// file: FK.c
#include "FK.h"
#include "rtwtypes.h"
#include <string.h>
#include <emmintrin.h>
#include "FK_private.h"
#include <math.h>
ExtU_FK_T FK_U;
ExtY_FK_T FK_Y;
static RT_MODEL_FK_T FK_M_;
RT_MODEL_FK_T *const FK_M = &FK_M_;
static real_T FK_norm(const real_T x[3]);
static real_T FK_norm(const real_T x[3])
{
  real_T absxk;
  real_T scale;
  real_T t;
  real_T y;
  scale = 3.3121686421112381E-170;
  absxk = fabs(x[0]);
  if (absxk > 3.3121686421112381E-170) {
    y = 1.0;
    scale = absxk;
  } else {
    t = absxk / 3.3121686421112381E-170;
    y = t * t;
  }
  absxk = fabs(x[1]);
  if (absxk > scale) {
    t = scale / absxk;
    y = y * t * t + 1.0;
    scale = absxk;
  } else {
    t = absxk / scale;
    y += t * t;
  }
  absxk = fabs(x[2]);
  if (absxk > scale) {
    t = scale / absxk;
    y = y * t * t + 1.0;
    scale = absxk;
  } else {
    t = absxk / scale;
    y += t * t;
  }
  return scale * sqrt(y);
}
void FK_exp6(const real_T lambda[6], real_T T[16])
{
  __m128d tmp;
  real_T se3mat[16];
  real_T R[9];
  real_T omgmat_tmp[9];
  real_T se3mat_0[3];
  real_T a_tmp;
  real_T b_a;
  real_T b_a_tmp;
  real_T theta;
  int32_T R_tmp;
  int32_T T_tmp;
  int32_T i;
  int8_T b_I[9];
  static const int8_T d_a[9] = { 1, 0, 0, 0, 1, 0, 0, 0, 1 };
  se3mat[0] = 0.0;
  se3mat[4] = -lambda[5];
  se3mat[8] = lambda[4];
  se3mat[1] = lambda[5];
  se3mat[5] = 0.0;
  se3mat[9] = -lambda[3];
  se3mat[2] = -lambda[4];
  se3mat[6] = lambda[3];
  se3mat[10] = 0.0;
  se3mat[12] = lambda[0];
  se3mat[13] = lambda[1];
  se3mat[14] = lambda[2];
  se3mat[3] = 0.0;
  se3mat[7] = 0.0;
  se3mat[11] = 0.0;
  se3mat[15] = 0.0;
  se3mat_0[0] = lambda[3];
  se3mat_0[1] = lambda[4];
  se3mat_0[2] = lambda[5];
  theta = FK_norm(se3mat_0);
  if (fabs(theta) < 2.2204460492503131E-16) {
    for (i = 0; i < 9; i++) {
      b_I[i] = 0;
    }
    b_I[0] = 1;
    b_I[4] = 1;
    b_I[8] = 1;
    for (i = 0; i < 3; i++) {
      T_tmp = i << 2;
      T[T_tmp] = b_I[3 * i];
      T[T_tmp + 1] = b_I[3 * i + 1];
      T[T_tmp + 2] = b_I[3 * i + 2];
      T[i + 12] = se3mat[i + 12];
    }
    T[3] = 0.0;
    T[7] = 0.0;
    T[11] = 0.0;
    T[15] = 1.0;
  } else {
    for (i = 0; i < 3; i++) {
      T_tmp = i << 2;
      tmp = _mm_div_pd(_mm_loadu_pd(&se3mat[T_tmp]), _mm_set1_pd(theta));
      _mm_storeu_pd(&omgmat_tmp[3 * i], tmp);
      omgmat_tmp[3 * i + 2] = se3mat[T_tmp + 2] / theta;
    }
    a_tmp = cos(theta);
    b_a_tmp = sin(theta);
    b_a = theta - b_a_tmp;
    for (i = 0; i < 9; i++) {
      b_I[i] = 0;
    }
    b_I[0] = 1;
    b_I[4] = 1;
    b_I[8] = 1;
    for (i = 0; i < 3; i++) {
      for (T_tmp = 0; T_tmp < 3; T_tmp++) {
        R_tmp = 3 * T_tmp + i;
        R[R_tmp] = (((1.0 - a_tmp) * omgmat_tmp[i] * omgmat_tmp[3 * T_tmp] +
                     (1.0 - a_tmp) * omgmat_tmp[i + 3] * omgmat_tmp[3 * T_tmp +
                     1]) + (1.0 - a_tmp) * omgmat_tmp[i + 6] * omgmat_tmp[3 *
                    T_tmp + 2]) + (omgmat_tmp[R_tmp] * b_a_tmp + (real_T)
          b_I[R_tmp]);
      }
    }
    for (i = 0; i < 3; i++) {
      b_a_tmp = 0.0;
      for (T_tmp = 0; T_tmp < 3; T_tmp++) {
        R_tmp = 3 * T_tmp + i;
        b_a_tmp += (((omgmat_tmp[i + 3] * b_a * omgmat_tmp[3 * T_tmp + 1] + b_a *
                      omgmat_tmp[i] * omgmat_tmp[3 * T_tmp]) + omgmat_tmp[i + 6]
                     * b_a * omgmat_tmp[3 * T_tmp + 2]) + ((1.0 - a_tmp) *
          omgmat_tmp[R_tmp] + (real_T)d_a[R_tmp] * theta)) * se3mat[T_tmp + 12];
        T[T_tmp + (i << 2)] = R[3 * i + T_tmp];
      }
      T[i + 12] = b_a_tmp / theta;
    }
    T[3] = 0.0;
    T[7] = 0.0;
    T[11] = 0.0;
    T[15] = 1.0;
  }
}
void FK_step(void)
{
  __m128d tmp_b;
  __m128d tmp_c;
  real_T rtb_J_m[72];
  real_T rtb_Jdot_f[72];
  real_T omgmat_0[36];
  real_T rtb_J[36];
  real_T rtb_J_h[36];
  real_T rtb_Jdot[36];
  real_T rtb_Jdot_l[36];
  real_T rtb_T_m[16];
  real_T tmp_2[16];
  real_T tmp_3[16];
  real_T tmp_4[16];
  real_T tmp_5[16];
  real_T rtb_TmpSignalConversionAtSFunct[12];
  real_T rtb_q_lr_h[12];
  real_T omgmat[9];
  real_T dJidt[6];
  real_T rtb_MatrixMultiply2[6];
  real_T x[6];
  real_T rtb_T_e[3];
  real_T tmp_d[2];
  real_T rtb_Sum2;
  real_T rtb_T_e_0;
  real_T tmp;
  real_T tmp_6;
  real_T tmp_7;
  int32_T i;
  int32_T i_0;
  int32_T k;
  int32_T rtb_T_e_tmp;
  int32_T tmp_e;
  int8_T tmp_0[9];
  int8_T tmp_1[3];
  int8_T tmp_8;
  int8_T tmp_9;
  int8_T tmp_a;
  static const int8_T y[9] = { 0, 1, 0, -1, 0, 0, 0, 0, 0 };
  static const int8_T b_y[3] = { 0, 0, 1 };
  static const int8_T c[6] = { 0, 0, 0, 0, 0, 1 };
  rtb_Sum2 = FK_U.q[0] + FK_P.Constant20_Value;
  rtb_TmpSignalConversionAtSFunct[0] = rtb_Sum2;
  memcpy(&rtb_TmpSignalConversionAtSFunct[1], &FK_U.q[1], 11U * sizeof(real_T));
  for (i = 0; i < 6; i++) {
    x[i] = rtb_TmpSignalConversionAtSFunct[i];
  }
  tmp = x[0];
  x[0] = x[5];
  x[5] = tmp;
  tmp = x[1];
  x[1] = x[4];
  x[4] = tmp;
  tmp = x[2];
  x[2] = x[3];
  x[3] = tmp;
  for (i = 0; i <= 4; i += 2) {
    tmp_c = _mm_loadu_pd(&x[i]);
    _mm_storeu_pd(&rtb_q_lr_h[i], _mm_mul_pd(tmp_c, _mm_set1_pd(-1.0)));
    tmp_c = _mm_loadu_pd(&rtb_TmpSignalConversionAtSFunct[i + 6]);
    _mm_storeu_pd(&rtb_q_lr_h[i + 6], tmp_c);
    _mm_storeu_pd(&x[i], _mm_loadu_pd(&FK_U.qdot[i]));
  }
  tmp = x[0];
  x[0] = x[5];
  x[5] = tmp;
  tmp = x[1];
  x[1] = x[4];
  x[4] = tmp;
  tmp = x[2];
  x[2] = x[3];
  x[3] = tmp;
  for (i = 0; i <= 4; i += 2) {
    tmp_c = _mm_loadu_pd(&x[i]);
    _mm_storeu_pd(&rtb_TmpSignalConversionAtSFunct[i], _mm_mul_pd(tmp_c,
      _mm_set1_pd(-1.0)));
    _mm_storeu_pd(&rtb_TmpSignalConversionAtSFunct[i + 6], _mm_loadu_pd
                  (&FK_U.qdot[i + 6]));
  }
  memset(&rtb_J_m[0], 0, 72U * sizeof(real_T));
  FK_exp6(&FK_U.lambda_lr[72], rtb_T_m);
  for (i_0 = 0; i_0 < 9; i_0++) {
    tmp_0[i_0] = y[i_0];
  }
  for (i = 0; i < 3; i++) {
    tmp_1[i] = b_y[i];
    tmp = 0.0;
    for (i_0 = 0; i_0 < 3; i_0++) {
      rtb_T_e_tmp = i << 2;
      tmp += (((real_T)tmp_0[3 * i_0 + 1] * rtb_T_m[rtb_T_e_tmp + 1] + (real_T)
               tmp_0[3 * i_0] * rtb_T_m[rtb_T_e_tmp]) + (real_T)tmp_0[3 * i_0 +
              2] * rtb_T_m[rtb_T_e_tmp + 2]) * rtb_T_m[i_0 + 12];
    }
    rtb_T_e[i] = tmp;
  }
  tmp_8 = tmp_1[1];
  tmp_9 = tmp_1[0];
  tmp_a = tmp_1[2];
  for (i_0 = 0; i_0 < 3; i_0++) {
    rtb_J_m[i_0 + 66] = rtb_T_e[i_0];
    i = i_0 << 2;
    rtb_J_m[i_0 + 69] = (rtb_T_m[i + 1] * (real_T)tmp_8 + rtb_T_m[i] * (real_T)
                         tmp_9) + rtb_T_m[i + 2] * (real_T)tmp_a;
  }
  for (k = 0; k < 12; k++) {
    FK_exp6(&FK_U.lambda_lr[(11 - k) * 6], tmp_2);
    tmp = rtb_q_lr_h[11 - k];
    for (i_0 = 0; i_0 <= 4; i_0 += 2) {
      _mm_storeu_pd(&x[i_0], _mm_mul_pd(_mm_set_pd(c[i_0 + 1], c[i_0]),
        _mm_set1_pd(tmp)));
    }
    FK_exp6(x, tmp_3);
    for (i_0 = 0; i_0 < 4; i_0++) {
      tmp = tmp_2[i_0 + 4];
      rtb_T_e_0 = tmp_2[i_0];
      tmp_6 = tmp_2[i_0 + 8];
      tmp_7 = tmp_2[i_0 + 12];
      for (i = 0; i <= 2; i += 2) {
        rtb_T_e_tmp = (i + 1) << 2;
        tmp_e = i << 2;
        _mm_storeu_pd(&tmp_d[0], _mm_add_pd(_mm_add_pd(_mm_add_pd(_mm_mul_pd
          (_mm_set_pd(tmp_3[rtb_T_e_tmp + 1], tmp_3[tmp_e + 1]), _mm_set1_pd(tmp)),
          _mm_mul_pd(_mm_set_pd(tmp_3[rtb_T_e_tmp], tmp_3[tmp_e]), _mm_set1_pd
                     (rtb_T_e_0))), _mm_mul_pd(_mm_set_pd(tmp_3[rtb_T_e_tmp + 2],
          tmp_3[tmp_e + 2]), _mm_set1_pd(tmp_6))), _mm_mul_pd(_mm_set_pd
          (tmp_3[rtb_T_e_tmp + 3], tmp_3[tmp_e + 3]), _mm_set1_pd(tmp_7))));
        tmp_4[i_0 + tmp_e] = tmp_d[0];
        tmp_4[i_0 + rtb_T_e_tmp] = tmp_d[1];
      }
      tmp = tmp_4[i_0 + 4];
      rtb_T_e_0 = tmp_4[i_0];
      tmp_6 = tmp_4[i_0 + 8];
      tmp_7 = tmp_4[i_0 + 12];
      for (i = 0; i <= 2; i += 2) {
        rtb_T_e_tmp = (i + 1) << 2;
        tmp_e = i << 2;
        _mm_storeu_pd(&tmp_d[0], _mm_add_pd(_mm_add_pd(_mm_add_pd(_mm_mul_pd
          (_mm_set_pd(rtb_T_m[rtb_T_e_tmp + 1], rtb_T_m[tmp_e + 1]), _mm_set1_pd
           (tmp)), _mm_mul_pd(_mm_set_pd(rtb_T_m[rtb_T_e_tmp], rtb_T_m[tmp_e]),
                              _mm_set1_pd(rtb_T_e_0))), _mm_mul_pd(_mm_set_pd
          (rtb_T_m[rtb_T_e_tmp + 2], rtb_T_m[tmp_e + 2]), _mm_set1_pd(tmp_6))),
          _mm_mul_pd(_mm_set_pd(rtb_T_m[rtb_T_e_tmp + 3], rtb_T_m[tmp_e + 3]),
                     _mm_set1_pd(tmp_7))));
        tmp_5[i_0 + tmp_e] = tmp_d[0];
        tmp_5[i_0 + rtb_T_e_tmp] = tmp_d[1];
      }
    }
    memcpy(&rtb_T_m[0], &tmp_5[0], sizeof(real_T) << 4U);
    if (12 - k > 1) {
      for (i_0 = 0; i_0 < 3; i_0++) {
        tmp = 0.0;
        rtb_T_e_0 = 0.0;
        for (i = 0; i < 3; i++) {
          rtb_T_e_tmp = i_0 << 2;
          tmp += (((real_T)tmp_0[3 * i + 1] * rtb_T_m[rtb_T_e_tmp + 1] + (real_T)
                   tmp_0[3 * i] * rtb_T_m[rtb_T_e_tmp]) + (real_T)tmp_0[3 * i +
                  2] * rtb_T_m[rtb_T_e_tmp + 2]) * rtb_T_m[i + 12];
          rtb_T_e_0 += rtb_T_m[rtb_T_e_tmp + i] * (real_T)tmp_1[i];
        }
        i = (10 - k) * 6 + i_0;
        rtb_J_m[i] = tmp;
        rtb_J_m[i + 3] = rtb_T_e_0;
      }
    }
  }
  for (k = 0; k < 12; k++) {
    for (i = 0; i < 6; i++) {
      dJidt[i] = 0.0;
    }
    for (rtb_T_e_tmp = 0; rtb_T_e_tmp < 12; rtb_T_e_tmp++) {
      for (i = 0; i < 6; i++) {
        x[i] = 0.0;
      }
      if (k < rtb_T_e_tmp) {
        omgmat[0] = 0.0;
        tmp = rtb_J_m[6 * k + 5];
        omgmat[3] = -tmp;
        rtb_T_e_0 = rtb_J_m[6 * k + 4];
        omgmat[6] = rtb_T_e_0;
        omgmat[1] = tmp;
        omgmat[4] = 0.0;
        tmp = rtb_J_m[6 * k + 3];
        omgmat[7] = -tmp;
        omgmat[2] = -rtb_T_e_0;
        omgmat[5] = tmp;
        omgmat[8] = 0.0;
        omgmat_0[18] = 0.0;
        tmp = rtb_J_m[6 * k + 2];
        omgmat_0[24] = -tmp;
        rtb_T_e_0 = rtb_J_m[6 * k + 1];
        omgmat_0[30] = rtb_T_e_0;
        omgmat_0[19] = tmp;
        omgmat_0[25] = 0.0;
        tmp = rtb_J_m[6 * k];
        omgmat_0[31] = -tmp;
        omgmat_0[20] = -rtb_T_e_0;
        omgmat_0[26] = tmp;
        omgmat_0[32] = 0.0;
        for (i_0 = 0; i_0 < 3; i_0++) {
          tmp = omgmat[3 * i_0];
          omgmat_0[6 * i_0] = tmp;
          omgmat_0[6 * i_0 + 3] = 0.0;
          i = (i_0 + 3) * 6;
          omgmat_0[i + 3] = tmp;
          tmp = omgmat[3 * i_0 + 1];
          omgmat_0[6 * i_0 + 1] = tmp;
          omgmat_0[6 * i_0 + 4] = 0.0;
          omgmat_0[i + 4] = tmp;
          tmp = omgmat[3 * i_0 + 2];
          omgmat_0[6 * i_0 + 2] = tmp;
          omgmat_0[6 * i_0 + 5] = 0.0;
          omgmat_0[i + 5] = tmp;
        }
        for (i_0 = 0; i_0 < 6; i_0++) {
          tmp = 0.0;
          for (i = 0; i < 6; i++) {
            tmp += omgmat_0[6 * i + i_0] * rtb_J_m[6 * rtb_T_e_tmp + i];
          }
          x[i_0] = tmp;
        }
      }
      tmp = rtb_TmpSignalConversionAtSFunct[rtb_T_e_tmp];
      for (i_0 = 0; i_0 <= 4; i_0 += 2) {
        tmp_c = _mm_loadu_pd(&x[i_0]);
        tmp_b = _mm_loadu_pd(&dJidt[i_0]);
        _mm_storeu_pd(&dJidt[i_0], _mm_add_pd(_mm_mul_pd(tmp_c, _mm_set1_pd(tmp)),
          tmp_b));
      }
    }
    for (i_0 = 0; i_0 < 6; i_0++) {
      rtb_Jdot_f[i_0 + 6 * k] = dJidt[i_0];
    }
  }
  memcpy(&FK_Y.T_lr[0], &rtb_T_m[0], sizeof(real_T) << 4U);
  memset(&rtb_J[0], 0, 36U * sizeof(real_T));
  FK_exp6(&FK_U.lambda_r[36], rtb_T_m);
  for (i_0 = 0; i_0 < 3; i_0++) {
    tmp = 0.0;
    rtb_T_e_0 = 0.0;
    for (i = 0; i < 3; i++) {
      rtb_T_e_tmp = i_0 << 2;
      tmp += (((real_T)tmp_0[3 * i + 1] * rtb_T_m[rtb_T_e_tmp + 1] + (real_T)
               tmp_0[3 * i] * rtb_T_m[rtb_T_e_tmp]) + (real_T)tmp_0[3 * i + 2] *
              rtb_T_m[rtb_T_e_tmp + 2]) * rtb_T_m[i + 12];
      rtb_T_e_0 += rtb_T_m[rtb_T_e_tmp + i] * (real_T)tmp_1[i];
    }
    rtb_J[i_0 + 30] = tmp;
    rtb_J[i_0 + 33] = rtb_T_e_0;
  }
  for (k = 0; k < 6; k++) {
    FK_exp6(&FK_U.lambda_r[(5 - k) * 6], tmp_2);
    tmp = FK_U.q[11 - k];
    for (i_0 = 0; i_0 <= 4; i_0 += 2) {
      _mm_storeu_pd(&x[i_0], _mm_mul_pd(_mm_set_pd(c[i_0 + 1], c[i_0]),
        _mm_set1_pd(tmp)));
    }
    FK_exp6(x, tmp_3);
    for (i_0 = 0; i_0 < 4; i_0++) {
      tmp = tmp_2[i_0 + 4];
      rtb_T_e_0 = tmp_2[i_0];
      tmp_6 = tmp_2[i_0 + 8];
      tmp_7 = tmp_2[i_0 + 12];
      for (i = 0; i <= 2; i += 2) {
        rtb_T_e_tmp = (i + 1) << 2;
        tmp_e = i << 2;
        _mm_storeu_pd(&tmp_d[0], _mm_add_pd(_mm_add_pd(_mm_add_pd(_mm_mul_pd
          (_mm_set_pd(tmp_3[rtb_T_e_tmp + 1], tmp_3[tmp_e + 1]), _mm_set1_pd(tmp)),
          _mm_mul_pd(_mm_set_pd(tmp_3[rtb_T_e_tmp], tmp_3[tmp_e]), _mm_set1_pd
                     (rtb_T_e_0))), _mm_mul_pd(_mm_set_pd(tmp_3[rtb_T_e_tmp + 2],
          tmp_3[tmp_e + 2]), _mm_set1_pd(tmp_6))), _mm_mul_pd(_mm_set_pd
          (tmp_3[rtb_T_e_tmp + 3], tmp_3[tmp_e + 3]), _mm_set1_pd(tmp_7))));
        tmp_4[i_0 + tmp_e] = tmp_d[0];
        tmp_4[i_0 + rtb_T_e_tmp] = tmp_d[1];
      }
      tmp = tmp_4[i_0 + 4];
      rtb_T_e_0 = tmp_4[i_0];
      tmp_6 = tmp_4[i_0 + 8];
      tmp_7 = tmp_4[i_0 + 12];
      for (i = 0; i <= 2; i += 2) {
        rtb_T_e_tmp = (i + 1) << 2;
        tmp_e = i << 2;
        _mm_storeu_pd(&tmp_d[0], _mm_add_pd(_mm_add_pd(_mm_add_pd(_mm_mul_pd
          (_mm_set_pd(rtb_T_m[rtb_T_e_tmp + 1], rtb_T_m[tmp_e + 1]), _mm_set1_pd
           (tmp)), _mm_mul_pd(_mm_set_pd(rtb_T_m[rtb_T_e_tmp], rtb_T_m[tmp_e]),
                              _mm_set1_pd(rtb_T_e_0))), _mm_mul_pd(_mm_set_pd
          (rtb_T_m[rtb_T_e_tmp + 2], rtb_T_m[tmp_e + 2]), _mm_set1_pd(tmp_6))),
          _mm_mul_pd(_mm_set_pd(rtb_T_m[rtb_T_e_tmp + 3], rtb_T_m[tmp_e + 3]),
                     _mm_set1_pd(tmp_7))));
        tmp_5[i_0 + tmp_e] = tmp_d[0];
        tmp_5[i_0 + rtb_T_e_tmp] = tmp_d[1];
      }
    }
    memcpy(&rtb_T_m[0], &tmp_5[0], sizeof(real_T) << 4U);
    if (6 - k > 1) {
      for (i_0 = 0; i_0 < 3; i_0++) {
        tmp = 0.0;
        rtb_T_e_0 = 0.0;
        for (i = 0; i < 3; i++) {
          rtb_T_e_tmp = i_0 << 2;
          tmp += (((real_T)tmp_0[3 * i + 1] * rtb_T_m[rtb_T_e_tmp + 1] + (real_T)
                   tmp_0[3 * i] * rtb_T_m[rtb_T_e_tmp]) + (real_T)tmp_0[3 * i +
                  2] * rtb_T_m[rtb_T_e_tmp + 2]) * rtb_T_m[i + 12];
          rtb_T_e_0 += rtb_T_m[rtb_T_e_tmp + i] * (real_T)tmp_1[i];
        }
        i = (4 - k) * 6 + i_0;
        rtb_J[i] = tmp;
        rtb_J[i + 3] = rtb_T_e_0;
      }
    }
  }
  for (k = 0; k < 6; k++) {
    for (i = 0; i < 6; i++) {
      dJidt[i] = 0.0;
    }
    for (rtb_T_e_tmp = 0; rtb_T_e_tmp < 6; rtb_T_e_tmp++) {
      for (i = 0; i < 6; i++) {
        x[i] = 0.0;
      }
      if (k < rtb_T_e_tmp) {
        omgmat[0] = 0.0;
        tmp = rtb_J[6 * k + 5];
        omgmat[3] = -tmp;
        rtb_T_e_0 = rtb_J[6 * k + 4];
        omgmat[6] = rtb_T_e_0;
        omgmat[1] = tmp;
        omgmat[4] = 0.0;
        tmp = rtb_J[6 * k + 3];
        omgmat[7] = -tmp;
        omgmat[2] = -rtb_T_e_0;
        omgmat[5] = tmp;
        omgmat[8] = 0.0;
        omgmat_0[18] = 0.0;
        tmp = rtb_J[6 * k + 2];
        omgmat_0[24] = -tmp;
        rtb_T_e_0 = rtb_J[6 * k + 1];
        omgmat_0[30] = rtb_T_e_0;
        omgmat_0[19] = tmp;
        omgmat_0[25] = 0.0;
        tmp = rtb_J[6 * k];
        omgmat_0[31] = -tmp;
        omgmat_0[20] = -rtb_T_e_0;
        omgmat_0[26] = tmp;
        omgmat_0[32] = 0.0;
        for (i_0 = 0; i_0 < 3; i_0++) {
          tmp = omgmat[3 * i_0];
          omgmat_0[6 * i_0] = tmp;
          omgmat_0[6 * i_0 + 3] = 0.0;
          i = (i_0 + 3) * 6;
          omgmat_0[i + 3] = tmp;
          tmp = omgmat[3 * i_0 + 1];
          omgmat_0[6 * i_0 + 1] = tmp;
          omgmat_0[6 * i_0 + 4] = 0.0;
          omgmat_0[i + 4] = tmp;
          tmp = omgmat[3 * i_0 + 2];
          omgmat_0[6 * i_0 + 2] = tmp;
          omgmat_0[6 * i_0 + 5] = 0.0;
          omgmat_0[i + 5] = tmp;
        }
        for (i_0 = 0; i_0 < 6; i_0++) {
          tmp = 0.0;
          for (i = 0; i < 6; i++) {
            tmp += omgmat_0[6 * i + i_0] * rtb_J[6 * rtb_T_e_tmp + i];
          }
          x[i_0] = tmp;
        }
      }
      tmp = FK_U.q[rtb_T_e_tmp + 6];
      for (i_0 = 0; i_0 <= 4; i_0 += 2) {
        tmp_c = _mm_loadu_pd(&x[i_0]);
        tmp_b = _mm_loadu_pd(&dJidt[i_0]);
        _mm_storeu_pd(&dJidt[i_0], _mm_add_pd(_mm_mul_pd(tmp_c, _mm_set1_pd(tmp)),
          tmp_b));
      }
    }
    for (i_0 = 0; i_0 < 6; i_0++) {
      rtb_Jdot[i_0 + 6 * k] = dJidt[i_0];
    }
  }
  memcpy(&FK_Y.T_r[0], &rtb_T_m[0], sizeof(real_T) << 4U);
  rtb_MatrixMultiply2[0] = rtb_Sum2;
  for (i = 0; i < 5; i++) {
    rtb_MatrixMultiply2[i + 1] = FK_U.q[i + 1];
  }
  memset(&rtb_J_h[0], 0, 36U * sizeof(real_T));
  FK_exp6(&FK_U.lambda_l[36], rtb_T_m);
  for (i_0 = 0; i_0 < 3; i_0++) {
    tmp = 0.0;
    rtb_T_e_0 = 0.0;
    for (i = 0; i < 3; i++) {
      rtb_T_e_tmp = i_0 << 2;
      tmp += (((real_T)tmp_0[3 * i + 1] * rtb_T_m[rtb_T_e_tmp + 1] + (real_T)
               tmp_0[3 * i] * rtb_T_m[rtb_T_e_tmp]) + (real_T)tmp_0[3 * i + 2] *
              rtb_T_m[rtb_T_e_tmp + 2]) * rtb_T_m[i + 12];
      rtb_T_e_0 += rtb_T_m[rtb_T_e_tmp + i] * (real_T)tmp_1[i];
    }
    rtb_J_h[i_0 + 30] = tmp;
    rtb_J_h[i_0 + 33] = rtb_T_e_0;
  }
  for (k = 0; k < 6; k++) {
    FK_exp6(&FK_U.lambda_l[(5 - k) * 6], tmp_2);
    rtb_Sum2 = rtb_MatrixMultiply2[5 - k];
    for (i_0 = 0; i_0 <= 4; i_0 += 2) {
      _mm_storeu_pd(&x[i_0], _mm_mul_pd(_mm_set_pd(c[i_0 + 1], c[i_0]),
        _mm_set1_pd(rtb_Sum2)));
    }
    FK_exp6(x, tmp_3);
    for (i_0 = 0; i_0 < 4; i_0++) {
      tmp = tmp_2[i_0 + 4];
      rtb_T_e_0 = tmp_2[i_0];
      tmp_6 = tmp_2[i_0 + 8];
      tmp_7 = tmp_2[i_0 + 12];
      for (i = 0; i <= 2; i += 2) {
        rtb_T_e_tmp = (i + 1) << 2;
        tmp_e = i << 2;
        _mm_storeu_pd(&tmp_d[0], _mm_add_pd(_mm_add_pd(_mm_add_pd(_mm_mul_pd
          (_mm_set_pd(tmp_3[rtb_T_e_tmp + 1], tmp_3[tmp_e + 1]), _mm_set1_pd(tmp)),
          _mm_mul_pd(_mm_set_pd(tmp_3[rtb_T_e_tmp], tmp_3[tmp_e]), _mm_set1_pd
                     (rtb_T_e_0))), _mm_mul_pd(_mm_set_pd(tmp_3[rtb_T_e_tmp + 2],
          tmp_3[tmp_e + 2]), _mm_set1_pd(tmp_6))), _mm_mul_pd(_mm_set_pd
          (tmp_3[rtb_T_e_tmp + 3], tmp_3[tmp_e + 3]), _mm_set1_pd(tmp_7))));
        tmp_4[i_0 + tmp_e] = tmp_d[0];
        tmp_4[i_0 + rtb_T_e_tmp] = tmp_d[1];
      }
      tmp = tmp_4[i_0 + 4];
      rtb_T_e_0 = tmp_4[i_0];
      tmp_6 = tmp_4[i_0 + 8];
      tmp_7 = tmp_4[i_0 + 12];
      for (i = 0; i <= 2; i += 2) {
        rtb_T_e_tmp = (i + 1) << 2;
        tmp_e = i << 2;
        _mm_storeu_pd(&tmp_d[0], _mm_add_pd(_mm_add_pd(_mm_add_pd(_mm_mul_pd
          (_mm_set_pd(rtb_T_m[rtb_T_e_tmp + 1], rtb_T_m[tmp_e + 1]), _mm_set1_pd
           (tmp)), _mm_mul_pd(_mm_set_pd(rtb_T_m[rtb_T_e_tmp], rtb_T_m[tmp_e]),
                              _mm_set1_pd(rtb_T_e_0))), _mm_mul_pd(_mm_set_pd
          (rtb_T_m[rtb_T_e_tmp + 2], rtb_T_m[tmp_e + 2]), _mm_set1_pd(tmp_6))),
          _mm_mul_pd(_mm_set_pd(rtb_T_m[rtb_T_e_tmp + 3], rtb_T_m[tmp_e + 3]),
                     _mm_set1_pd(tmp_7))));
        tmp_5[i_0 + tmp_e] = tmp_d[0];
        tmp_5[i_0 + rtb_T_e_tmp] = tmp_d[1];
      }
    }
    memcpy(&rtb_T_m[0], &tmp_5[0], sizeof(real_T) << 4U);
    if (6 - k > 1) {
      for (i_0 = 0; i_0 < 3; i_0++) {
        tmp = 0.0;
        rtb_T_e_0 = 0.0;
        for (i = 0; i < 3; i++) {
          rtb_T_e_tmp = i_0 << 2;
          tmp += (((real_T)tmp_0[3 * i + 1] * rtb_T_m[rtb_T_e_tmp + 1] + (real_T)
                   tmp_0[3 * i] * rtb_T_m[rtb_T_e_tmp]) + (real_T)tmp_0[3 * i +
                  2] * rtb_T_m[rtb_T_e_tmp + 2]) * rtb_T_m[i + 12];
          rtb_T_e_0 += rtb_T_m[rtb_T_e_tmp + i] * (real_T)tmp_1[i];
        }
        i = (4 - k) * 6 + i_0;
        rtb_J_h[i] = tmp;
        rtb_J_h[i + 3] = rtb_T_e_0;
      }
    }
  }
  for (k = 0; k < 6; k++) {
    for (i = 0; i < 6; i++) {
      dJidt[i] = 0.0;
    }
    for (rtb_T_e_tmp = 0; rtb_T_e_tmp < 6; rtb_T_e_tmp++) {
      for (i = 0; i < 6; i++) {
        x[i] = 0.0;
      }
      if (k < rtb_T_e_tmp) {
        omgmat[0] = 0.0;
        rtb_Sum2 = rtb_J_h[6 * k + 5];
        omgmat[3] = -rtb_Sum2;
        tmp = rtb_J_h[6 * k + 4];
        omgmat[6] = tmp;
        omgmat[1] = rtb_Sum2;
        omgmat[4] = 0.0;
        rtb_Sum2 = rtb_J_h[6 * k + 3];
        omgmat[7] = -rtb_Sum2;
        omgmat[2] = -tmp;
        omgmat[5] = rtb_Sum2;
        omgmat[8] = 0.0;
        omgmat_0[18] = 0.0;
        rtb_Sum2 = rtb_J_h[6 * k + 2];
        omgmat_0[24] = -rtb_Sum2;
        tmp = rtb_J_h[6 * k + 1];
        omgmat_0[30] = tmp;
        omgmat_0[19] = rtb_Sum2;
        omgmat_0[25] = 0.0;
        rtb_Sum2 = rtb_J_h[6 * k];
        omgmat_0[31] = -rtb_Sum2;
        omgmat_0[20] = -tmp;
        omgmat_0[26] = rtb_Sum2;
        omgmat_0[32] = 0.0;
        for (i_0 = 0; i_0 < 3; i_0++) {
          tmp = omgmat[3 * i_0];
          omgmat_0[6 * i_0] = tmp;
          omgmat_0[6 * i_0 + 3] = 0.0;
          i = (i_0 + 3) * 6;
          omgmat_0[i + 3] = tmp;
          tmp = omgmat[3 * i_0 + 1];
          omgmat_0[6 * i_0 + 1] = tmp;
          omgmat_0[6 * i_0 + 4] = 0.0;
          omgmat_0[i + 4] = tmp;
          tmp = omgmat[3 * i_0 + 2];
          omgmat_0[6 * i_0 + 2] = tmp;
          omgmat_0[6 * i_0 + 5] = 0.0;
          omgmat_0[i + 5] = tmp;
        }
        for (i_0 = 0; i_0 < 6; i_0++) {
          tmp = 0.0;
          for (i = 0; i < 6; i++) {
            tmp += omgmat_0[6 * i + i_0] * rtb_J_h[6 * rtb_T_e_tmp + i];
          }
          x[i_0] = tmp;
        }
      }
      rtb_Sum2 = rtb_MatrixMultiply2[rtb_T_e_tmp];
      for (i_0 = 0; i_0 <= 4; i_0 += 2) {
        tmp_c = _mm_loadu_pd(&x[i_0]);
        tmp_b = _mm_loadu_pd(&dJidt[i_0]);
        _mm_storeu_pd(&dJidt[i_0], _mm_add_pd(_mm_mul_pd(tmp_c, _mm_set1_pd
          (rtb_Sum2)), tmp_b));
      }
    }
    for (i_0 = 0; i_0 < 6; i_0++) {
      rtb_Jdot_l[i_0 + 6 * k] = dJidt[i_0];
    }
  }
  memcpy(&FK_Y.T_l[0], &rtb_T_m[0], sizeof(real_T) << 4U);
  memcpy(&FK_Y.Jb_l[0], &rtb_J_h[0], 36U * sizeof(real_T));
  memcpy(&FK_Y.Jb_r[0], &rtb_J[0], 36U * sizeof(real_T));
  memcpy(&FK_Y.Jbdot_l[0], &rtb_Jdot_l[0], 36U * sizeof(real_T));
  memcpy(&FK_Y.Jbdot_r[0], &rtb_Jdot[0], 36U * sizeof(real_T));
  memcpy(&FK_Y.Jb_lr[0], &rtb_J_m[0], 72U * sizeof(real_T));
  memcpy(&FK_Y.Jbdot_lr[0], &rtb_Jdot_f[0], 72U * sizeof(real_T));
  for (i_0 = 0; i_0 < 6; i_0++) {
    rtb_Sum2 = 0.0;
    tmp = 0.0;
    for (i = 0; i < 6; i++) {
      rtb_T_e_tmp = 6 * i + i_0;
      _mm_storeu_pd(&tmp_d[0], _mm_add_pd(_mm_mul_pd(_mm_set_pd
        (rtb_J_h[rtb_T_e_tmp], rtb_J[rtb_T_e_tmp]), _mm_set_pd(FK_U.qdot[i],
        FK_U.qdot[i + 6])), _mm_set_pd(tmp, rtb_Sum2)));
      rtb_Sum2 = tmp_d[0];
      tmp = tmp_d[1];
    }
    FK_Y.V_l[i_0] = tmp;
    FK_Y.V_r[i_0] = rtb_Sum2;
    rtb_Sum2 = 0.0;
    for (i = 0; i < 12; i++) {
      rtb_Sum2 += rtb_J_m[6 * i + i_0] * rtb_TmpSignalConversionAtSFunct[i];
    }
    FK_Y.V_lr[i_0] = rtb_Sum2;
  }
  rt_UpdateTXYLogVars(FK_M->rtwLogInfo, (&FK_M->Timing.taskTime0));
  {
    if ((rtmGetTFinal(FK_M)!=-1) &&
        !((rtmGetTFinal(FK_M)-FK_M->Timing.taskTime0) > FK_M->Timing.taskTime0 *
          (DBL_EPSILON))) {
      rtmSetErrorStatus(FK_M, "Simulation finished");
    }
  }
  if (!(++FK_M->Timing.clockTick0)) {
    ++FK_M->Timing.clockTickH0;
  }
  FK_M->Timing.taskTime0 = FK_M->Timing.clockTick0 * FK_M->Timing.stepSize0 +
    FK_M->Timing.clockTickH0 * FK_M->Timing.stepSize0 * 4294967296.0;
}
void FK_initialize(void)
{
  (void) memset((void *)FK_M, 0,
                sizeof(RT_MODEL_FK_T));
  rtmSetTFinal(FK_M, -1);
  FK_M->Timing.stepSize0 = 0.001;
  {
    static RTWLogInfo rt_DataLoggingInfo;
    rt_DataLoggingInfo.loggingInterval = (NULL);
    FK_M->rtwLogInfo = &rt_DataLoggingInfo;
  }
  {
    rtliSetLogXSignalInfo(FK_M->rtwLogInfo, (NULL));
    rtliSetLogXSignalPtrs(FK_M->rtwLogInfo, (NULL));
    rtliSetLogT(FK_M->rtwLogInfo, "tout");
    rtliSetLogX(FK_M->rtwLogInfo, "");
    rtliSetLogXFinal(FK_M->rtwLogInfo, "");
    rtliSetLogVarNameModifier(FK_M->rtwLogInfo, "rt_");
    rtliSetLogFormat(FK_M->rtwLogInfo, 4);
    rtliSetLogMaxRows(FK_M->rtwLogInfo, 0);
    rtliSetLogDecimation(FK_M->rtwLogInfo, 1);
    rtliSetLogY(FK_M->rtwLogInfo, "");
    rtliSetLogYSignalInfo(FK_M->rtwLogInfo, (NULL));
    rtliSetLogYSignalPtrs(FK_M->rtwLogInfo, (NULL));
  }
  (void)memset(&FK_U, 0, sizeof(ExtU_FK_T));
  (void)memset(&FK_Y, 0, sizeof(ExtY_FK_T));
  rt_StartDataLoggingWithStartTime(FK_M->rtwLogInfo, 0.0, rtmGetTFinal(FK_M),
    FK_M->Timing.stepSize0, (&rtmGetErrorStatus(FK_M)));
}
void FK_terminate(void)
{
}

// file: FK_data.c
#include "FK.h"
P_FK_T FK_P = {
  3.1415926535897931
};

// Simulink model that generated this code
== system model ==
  Inport#1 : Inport
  qdot : Inport
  lambda_lr : Inport
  lambda_l : Inport
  lambda_r : Inport
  T_lr : Outport  <- 1: MATLABFunction#1/3
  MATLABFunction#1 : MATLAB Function  <- 1: lambda_lr, 2: MATLABFunction#2, 3: MATLABFunction#3
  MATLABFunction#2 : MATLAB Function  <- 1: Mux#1
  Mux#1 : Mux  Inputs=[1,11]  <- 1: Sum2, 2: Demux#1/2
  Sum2 : Sum  Inputs=++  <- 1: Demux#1, 2: Constant20
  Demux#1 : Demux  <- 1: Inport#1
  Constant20 : Constant  Value=pi
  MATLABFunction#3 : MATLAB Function  <- 1: qdot
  T_r : Outport  <- 1: MATLABFunction#4/3
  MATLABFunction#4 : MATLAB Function  <- 1: lambda_r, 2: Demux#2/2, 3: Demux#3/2
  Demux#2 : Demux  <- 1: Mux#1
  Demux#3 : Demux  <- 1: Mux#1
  T_l : Outport  <- 1: MATLABFunction#5/3
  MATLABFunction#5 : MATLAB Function  <- 1: lambda_l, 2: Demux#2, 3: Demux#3
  Jb_l : Outport  <- 1: MATLABFunction#5/2
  Jb_r : Outport  <- 1: MATLABFunction#4/2
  Jbdot_l : Outport  <- 1: MATLABFunction#5
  Jbdot_r : Outport  <- 1: MATLABFunction#4
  Jb_lr : Outport  <- 1: MATLABFunction#1/2
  Jbdot_lr : Outport  <- 1: MATLABFunction#1
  V_r : Outport  <- 1: Product#1
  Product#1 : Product  Multiplication=Matrix(*)  <- 1: MATLABFunction#4/2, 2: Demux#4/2
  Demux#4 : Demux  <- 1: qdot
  V_l : Outport  <- 1: Product#2
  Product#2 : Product  Multiplication=Matrix(*)  <- 1: MATLABFunction#5/2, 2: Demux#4
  V_lr : Outport  <- 1: MatrixMultiply2
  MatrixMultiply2 : Product  Multiplication=Matrix(*)  <- 1: MATLABFunction#1/2, 2: MATLABFunction#3
== matlab function MATLABFunction#2 ==
function q_lr = getQrel(q)
q_lr = zeros(12,1);
q_lr = [-flip(q(1:6));q(7:end)];

== matlab function MATLABFunction#1 ==
function [Jdot,J,T]=FKJacobian(lambda_list,q,q_dot)
    Ti = eye(4);
    [m,n]=size(lambda_list);
    lamda_z = [0,0,0,0,0,1]';
    ez = [0,0,1]';
    N = length(q);
    J = zeros(6,N);
    Jdot=zeros(6,N);
  
    Ti = exp6(lambda_list(:,end));
    [Ri,pi] = TransToRp(Ti);
    J(:,end)=[Ri'*VecToso3(ez)*pi;Ri'*ez];
    for i =N:-1:1
        Ti = exp6(lambda_list(:,i))*exp6(lamda_z*q(i))*Ti;
 
        [Ri,pi] = TransToRp(Ti);
        if i>1
            J(:,i-1)=[Ri'*VecToso3(ez)*pi;Ri'*ez];
        end

    end
    for i=1:1:N
        Ji = J(:,i);
        dJidt = zeros(6,1);
        for j=1:1:N
            Jj = J(:,j);
            aJiaqj = zeros(6,1);
            if(i<j) 
                aJiaqj = ad(Ji)*Jj;
            end
            dJidt = dJidt+aJiaqj*q_dot(j);
        end
        Jdot(:,i) = dJidt;
    end
    T = Ti;
end

== matlab function MATLABFunction#3 ==
function q_lr = getQrel(q)
q_lr = zeros(12,1);
q_lr = [-flip(q(1:6));q(7:end)];

== matlab function MATLABFunction#5 ==
function [Jdot,J,T]=FKJacobian(lambda_list,q,q_dot)
    Ti = eye(4);
    [m,n]=size(lambda_list);
    lamda_z = [0,0,0,0,0,1]';
    ez = [0,0,1]';
    N = length(q);
    J = zeros(6,N);
    Jdot=zeros(6,N);
  
    Ti = exp6(lambda_list(:,end));
    [Ri,pi] = TransToRp(Ti);
    J(:,end)=[Ri'*VecToso3(ez)*pi;Ri'*ez];
    for i =N:-1:1
        Ti = exp6(lambda_list(:,i))*exp6(lamda_z*q(i))*Ti;
 
        [Ri,pi] = TransToRp(Ti);
        if i>1
            J(:,i-1)=[Ri'*VecToso3(ez)*pi;Ri'*ez];
        end

    end
    for i=1:1:N
        Ji = J(:,i);
        dJidt = zeros(6,1);
        for j=1:1:N
            Jj = J(:,j);
            aJiaqj = zeros(6,1);
            if(i<j) 
                aJiaqj = ad(Ji)*Jj;
            end
            dJidt = dJidt+aJiaqj*q_dot(j);
        end
        Jdot(:,i) = dJidt;
    end
    T = Ti;
end

== matlab function MATLABFunction#4 ==
function [Jdot,J,T]=FKJacobian(lambda_list,q,q_dot)
    Ti = eye(4);
    [m,n]=size(lambda_list);
    lamda_z = [0,0,0,0,0,1]';
    ez = [0,0,1]';
    N = length(q);
    J = zeros(6,N);
    Jdot=zeros(6,N);
  
    Ti = exp6(lambda_list(:,end));
    [Ri,pi] = TransToRp(Ti);
    J(:,end)=[Ri'*VecToso3(ez)*pi;Ri'*ez];
    for i =N:-1:1
        Ti = exp6(lambda_list(:,i))*exp6(lamda_z*q(i))*Ti;
 
        [Ri,pi] = TransToRp(Ti);
        if i>1
            J(:,i-1)=[Ri'*VecToso3(ez)*pi;Ri'*ez];
        end

    end
    for i=1:1:N
        Ji = J(:,i);
        dJidt = zeros(6,1);
        for j=1:1:N
            Jj = J(:,j);
            aJiaqj = zeros(6,1);
            if(i<j) 
                aJiaqj = ad(Ji)*Jj;
            end
            dJidt = dJidt+aJiaqj*q_dot(j);
        end
        Jdot(:,i) = dJidt;
    end
    T = Ti;
end
